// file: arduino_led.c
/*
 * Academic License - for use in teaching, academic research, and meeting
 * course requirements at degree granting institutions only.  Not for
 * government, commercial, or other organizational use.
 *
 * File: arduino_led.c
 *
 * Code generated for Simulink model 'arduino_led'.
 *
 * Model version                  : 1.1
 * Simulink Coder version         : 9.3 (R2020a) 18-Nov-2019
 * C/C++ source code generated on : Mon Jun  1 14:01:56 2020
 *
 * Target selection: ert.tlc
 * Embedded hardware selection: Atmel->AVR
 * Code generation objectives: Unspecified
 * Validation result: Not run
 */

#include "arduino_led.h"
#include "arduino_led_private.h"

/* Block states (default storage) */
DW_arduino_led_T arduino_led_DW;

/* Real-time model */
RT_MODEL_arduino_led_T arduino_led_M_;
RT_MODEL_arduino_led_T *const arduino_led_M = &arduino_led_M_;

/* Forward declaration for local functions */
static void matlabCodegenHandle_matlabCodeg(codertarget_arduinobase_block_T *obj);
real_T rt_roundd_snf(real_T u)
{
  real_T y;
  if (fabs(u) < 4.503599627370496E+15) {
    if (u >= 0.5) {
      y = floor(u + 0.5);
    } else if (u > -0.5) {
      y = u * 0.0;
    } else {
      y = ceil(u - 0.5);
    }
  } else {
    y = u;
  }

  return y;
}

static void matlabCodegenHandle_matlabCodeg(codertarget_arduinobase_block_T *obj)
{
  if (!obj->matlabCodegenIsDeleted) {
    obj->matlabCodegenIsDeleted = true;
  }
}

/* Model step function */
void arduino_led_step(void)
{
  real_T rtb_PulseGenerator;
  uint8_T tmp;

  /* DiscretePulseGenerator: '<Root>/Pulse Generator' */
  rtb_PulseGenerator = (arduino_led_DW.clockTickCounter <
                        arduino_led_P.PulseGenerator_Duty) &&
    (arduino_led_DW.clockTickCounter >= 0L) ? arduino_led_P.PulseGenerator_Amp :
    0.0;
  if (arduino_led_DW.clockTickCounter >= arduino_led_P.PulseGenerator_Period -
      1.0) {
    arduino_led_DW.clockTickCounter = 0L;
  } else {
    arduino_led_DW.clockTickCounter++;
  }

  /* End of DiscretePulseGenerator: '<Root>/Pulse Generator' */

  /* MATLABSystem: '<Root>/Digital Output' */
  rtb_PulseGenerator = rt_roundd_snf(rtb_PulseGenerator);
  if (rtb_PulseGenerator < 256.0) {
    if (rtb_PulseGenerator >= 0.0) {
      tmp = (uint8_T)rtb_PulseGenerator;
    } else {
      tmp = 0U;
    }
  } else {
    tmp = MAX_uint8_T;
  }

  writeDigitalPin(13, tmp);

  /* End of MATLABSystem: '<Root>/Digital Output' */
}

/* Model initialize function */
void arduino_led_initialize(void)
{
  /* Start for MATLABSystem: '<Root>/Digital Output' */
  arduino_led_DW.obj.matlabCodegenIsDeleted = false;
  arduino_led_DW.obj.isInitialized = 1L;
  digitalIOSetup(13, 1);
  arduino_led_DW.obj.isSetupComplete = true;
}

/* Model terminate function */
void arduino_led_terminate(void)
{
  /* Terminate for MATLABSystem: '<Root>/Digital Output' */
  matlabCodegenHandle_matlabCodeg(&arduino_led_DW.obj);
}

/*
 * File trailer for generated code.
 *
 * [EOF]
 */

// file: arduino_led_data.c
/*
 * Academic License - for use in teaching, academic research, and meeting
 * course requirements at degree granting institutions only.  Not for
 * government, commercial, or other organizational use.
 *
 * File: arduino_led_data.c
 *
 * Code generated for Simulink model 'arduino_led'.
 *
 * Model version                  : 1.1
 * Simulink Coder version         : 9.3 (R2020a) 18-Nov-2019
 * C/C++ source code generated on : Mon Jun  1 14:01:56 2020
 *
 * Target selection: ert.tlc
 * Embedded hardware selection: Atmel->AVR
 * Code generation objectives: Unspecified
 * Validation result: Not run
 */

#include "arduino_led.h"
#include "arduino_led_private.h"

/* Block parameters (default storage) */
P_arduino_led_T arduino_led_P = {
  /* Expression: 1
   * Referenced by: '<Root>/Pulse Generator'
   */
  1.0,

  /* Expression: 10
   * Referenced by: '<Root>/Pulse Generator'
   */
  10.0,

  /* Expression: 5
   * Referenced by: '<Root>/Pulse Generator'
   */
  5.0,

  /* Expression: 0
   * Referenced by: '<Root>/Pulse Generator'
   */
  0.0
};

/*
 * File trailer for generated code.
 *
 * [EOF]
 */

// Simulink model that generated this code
simulink model "arduino_led"  (R2020a)
settings: Solver=VariableStepAuto  StartTime=0.0  StopTime=10.0  RelTol=1e-3
libraries: arduinolib x1

== system arduino_led ==
  Digital Output : arduinolib/Digital Output  pinNumber=13  Direction=output  blockPlatform=arduino
  Pulse Generator : DiscretePulseGenerator  Period=10  PulseWidth=5  SampleTime=0.1
  wires:
  Pulse Generator/1 -> Digital Output/1
